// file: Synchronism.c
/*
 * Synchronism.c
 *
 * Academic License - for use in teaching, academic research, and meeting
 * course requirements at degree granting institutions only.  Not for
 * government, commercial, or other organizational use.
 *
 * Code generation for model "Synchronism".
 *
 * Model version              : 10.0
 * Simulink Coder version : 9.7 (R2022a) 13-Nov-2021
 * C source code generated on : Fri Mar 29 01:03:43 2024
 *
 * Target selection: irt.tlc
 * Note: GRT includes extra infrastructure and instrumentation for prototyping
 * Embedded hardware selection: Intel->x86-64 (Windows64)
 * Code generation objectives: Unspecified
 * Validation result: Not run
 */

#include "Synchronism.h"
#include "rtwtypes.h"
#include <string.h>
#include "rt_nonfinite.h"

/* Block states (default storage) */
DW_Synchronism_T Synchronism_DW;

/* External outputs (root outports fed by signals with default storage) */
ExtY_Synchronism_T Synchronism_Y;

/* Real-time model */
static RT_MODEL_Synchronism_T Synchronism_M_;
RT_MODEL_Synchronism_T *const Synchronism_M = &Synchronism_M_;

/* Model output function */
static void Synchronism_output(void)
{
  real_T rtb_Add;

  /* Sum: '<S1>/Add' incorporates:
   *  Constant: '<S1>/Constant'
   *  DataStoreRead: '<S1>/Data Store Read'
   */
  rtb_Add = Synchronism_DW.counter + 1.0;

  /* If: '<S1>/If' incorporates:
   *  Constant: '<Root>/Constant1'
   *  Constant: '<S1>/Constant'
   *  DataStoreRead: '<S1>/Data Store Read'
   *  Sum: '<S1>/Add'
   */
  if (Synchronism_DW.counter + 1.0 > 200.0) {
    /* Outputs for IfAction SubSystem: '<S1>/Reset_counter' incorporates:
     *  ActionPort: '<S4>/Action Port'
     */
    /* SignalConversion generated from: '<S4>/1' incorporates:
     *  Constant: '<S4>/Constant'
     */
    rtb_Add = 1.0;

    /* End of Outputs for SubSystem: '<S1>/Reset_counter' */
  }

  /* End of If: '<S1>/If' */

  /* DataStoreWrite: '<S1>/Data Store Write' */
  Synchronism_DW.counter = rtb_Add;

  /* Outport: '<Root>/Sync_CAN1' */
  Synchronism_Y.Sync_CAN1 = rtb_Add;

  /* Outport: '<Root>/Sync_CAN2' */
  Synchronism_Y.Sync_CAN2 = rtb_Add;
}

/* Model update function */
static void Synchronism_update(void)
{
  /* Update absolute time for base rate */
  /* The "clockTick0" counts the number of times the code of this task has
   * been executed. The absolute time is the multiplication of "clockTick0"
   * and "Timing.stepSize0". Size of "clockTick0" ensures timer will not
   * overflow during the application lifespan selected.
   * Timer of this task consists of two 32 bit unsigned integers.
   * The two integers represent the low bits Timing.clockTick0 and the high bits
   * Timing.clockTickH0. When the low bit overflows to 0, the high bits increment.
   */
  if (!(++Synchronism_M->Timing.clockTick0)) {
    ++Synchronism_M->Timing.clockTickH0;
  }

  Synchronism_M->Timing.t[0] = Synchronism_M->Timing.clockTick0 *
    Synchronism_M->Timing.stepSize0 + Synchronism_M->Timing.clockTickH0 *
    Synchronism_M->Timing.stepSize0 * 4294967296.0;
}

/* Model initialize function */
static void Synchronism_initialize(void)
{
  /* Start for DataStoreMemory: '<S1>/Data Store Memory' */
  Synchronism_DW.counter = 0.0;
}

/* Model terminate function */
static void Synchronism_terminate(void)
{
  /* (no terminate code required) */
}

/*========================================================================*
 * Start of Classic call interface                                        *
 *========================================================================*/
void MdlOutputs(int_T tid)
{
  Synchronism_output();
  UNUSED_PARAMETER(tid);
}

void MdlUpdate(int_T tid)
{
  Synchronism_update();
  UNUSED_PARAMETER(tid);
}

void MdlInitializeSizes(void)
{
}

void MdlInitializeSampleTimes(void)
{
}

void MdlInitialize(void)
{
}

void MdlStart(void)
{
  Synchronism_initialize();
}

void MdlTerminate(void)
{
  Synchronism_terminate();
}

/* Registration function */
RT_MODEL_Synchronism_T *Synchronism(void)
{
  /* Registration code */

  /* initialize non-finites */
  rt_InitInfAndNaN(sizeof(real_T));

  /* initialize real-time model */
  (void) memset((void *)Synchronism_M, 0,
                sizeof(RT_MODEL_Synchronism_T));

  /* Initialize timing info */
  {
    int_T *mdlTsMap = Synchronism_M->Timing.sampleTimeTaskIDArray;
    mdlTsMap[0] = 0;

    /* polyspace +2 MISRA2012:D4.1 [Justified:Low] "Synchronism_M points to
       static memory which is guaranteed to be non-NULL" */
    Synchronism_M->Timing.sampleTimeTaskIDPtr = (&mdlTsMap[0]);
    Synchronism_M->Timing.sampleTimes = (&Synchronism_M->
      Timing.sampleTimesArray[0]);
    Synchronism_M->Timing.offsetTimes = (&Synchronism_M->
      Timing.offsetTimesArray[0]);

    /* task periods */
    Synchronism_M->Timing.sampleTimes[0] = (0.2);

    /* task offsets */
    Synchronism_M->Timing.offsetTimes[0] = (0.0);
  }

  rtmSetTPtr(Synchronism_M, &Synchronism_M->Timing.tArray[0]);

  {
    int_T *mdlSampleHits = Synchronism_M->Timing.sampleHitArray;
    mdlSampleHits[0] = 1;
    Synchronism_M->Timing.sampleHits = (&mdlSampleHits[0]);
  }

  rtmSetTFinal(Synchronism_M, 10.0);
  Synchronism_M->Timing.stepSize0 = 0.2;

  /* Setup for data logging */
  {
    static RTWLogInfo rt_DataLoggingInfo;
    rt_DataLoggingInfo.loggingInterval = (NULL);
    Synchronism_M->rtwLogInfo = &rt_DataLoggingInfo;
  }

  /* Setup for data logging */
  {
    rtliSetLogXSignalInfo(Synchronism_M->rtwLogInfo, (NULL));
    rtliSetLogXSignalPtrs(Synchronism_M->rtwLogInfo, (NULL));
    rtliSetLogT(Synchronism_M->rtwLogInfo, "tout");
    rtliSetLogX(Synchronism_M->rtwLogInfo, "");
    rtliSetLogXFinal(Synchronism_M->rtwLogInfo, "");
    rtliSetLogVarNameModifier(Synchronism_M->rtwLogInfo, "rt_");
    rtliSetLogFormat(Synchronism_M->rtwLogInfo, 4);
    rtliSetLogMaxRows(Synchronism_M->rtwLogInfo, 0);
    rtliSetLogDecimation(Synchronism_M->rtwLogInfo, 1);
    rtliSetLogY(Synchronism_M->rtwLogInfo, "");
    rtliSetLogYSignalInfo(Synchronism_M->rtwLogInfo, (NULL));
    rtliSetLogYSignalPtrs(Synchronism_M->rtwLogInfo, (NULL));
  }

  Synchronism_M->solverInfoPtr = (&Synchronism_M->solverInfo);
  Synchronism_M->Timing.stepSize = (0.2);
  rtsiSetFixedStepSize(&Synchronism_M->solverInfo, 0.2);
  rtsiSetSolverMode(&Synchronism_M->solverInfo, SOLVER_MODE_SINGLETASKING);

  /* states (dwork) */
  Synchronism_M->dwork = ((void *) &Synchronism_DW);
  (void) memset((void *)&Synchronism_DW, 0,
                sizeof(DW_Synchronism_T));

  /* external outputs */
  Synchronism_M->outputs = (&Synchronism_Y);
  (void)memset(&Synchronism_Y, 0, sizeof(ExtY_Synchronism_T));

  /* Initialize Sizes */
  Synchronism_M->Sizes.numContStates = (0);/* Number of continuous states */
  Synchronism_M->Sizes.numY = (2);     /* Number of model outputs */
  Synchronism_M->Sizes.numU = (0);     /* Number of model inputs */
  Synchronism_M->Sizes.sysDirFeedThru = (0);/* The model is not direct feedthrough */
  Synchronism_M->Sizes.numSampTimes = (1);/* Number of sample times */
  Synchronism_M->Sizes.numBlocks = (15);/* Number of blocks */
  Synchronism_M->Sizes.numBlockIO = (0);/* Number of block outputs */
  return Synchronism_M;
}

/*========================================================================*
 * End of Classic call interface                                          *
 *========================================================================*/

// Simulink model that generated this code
simulink model "Synchronism"  (R2022a)
settings: Solver=FixedStepAuto  StartTime=0.0  StopTime=10.0  RelTol=1e-3
libraries: simulink x1

== system Synchronism ==
  Constant1 : Constant  Value=200
  Counter : Subsystem
  Sync_CAN1 : Outport  VectorParamsAs1DForOutWhenUnconnected=off
  Sync_CAN2 : Outport  Port=2  VectorParamsAs1DForOutWhenUnconnected=off
  wires:
  Counter/1(Count) -> Sync_CAN2/1, Sync_CAN1/1
  Constant1/1 -> Counter/1(Module)

== system Synchronism/Counter ==
  Module : Inport
  Add : Sum
  Constant : Constant
  Counting : Subsystem  TreatAsAtomicUnit=on
  Data Store Memory : DataStoreMemory  DataStoreName=counter  ReadBeforeWriteMsg=warning  WriteAfterWriteMsg=warning  WriteAfterReadMsg=warning  ShowAdditionalParam=off
  Data Store Read : DataStoreRead  DataStoreName=counter  IndexOptions=Index vector (dialog)  Indices=1  OutputSizes=1
  Data Store Write : DataStoreWrite  DataStoreName=counter  IndexOptions=Index vector (dialog)  Indices=1  OutputSizes=1
  DocBlock : simulink/Model-Wide Utilities/DocBlock  DocumentType=Text
      content=|
      | Per generar la rampa es defineix un contador amb la variable counter
      |
      | Cada vegada que s'executa el model s'agafa el contador i es suma 1.
      | Si aquest valor és més gran que el mòdul del contador vol dir que hem de continuar contant,
      | sinó s'ha de resetejar el contador i posar-lo a 1.
  If : If  NumInputs=2  IfExpression=u1 < u2
  Merge3 : Merge
  Reset_counter : Subsystem  TreatAsAtomicUnit=on
  Count : Outport  VectorParamsAs1DForOutWhenUnconnected=off
  wires:
  Data Store Read/1 -> Add/1
  Constant/1 -> Add/2
  If/1 -> Reset_counter/Action
  If/2 -> Counting/Action
  Reset_counter/1(1) -> Merge3/1
  Counting/1(pass) -> Merge3/2
  Merge3/1 -> Data Store Write/1, Count/1
  Module/1 -> If/1
  Add/1 -> Counting/1(counter), If/2

== system Synchronism/Counter/Counting ==
  counter : Inport
  Action Port : ActionPort  ActionPortLabel=else { }
  pass : Outport  VectorParamsAs1DForOutWhenUnconnected=off
  wires:
  counter/1 -> pass/1

== system Synchronism/Counter/Reset_counter ==
  Action Port : ActionPort  ActionPortLabel=if { }
  Constant : Constant
  1 : Outport  VectorParamsAs1DForOutWhenUnconnected=off
  wires:
  Constant/1 -> 1/1
